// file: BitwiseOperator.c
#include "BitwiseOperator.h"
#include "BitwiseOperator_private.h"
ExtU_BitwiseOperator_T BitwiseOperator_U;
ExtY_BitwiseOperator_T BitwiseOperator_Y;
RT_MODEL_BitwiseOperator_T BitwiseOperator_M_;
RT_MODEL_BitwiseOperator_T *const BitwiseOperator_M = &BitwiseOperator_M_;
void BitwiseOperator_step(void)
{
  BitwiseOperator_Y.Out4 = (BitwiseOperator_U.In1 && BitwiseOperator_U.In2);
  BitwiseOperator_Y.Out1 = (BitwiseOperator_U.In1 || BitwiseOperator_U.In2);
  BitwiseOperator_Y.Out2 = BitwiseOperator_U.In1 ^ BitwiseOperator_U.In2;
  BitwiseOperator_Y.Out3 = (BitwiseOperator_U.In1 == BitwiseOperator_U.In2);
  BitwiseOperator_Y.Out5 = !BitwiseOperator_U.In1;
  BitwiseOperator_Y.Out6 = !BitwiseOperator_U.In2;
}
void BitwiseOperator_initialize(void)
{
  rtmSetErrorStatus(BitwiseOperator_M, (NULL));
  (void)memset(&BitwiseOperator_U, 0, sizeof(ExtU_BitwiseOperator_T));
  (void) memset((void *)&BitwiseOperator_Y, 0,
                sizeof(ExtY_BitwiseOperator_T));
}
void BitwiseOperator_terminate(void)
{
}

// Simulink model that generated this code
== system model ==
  In1 : Inport
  In2 : Inport
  Out4 : Outport  <- 1: BitwiseOperator
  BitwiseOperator : simulink/Logic and Bit Operations/Bitwise Operator  logicop=AND  BitMask=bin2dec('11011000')  <- 1: In1, 2: In2
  Out1 : Outport  <- 1: BitwiseOperator#1
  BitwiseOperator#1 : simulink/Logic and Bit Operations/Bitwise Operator  logicop=OR  BitMask=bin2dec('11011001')  <- 1: In1, 2: In2
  Out2 : Outport  <- 1: BitwiseOperator#2
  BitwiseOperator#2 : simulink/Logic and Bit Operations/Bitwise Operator  logicop=XOR  BitMask=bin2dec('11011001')  <- 1: In1, 2: In2
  Out3 : Outport  <- 1: BitwiseOperator#3
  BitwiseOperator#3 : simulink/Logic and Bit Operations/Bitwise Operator  logicop=NOR  BitMask=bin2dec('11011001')  <- 1: BitwiseOperator#4
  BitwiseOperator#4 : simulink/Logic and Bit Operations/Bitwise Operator  logicop=XOR  BitMask=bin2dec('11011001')  <- 1: In1, 2: In2
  Out5 : Outport  <- 1: Logic#1
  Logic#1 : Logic  Operator=NOT  <- 1: In1
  Out6 : Outport  <- 1: Logic#2
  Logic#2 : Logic  Operator=NOT  <- 1: In2
